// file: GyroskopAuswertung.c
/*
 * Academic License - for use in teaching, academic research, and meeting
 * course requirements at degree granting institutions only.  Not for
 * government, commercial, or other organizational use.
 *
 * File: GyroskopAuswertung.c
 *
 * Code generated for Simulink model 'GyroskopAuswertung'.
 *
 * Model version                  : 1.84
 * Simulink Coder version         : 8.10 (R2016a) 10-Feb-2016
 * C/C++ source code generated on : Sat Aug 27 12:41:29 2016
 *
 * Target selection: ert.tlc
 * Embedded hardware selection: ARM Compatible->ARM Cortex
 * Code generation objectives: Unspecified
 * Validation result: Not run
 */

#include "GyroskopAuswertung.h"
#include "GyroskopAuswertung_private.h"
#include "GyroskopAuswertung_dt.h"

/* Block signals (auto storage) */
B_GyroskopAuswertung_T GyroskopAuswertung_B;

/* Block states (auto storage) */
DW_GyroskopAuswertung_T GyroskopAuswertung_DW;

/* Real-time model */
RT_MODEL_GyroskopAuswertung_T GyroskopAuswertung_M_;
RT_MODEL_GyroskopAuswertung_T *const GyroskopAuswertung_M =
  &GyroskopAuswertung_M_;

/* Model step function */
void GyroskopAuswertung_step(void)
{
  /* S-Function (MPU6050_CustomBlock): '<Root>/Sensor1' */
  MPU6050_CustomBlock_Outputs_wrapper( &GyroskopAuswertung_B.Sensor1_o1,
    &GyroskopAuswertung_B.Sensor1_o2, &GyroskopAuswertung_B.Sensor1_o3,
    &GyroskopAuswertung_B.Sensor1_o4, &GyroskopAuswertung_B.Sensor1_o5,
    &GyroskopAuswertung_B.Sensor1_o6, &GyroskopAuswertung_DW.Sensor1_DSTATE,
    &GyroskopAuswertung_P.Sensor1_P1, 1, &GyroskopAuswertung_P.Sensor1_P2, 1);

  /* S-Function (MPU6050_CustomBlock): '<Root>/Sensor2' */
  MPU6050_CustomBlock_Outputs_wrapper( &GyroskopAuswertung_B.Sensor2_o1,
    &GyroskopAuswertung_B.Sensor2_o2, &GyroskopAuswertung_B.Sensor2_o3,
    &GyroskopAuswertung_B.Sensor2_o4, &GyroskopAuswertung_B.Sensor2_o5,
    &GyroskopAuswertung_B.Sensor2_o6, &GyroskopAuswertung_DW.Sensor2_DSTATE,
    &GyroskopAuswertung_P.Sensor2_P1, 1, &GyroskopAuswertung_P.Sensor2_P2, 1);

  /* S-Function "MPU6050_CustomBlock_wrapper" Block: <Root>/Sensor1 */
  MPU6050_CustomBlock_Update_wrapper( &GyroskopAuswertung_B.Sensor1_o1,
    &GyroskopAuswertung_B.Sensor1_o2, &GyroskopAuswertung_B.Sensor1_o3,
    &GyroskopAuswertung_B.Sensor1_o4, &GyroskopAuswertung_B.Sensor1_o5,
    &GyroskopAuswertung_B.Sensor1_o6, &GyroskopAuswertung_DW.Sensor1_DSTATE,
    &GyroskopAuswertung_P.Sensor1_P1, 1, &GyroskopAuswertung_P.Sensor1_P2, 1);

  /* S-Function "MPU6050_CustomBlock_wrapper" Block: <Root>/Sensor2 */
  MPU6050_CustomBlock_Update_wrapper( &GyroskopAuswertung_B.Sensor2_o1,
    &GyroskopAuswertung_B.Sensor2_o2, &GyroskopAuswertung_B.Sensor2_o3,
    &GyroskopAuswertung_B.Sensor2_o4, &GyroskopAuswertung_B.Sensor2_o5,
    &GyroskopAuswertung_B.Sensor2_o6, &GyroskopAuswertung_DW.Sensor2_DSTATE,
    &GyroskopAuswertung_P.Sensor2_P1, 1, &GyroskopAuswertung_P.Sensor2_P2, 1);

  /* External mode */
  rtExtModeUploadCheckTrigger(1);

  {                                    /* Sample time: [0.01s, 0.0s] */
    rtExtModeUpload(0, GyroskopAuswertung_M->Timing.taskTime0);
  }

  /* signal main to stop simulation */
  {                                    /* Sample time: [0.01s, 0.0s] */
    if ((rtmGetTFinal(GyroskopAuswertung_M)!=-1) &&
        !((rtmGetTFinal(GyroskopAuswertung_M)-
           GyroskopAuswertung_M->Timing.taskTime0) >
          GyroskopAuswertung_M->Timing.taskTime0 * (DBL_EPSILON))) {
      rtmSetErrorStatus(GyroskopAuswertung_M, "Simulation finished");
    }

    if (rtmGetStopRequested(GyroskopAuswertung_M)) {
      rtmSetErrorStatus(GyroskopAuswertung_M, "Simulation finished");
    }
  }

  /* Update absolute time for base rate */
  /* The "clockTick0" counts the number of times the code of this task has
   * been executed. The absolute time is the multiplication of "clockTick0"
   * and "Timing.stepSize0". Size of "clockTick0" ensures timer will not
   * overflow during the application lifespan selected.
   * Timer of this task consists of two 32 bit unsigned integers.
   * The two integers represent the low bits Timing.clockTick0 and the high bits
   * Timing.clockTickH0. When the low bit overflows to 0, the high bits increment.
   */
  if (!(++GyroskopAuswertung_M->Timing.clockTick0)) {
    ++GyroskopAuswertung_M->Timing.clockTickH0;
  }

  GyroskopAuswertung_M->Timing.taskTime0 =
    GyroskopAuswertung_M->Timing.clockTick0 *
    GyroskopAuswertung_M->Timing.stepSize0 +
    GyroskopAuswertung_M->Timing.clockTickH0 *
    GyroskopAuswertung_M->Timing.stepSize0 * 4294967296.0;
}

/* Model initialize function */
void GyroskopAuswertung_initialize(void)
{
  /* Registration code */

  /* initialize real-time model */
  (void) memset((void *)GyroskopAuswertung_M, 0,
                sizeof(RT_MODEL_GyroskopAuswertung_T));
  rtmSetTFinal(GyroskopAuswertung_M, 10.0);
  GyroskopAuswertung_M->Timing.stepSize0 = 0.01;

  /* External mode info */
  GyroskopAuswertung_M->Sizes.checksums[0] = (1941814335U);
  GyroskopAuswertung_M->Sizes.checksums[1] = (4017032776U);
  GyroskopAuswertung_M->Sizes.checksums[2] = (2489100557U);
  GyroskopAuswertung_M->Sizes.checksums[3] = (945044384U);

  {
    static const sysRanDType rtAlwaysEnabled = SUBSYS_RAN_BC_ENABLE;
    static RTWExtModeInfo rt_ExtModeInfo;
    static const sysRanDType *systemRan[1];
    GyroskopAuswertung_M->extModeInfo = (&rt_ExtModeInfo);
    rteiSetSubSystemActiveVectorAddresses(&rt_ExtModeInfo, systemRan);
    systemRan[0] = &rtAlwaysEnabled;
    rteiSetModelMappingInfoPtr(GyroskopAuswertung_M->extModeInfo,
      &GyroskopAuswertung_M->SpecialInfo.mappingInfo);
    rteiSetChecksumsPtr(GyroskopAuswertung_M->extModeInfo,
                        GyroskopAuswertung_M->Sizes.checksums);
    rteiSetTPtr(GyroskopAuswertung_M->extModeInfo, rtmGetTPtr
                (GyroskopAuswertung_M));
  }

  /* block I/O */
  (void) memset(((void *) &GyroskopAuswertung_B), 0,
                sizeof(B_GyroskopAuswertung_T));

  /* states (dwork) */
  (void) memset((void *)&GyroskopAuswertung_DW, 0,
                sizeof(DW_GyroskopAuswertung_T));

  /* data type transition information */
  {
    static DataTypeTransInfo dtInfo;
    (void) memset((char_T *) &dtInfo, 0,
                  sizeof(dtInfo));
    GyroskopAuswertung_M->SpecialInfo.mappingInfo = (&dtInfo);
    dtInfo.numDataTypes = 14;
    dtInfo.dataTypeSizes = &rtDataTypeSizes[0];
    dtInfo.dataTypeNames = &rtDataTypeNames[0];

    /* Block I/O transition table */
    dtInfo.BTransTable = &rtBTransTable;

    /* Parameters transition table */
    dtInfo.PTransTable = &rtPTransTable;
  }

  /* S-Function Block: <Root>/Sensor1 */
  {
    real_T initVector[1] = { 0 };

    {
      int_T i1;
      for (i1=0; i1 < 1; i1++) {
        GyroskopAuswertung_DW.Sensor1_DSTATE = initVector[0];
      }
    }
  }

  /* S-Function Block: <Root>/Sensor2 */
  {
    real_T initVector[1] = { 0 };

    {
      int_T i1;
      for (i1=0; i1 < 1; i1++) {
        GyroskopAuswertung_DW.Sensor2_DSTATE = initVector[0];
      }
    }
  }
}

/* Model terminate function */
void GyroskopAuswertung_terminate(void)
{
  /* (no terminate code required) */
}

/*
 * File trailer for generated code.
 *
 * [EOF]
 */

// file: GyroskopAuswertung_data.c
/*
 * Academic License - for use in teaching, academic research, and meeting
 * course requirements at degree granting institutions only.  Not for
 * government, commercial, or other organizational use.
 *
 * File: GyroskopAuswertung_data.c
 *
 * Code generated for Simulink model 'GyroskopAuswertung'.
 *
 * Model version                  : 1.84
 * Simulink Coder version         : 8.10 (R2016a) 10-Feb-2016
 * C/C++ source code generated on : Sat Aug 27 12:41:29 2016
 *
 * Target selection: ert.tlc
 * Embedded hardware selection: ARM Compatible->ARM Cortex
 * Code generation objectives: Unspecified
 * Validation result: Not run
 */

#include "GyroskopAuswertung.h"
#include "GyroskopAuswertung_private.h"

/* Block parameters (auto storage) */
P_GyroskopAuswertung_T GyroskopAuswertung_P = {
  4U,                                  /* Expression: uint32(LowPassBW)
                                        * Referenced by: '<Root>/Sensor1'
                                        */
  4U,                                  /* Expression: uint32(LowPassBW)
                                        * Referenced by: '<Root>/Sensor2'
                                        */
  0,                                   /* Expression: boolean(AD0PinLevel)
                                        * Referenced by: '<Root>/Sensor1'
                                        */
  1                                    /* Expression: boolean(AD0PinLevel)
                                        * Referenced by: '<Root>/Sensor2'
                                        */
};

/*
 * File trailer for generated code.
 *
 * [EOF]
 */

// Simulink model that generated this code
simulink model "GyroskopAuswertung"  (R2016a)
settings: Solver=FixedStepAuto  StartTime=0.0  StopTime=10  FixedStep=0.01  RelTol=1e-3
StopFcn:
  | AuswertungSensorenWinkelgeschwindigkeit

== system GyroskopAuswertung ==
  Sensor1 : S-Function  InitFcn=try, set_param(gcb,'FunctionName','MPU6050_CustomBlock'), end  FunctionName=MPU6050_CustomBlock  Parameters=boolean(AD0PinLevel),uint32(LowPassBW)  SFunctionModules=MPU6050_CustomBlock_wrapper  SFunctionDeploymentMode=off  EnableBusSupport=off  mask(S-Function Builder){AD0PinLevel=0, LowPassBW=44}
      mask prompts: AD0PinLevel "Logic-Level of AD0 Pin"; LowPassBW "Low-Pass-Bandwidth [Hz]"
      mask help: Simulink:masks:SFunctionBuilder_MD
      mask init:
      | val = [[.9  0.75 0.75 1 1 .9 .9 1]',[1 1 0.75 0.75 .9 .9 1 .9]'];try , sys = get_param(gcb,'SfunBuilderFcnName');if isempty(sys), sys = get_param(gcb,'FunctionName'); end,catch, sys = get_param(gcb,'FunctionName'); end
  Sensor2 : S-Function  InitFcn=try, set_param(gcb,'FunctionName','MPU6050_CustomBlock'), end  FunctionName=MPU6050_CustomBlock  Parameters=boolean(AD0PinLevel),uint32(LowPassBW)  SFunctionModules=MPU6050_CustomBlock_wrapper  SFunctionDeploymentMode=off  EnableBusSupport=off  mask(S-Function Builder){AD0PinLevel=1, LowPassBW=44}
      mask prompts: AD0PinLevel "Logic-Level of AD0 Pin"; LowPassBW "Low-Pass-Bandwidth [Hz]"
      mask help: Simulink:masks:SFunctionBuilder_MD
      mask init: same as GyroskopAuswertung/Sensor1
  Terminator{,1..6,8..10} (10 alike) : Terminator
  To Workspace1 : ToWorkspace  VariableName=phi2__d  SaveFormat=Structure With Time  SampleTime=-1
  To Workspace4 : ToWorkspace  VariableName=phi1__d  SaveFormat=Structure With Time  SampleTime=-1
  wires:
  Sensor2/1 -> Terminator10/1
  Sensor2/2 -> Terminator9/1
  Sensor2/4 -> Terminator5/1
  Sensor2/5 -> Terminator6/1
  Sensor2/6 -> To Workspace1/1
  Sensor1/3 -> Terminator/1
  Sensor1/4 -> Terminator1/1
  Sensor1/5 -> Terminator2/1
  Sensor1/6 -> To Workspace4/1
  Sensor2/3 -> Terminator4/1
  Sensor1/2 -> Terminator3/1
  Sensor1/1 -> Terminator8/1
